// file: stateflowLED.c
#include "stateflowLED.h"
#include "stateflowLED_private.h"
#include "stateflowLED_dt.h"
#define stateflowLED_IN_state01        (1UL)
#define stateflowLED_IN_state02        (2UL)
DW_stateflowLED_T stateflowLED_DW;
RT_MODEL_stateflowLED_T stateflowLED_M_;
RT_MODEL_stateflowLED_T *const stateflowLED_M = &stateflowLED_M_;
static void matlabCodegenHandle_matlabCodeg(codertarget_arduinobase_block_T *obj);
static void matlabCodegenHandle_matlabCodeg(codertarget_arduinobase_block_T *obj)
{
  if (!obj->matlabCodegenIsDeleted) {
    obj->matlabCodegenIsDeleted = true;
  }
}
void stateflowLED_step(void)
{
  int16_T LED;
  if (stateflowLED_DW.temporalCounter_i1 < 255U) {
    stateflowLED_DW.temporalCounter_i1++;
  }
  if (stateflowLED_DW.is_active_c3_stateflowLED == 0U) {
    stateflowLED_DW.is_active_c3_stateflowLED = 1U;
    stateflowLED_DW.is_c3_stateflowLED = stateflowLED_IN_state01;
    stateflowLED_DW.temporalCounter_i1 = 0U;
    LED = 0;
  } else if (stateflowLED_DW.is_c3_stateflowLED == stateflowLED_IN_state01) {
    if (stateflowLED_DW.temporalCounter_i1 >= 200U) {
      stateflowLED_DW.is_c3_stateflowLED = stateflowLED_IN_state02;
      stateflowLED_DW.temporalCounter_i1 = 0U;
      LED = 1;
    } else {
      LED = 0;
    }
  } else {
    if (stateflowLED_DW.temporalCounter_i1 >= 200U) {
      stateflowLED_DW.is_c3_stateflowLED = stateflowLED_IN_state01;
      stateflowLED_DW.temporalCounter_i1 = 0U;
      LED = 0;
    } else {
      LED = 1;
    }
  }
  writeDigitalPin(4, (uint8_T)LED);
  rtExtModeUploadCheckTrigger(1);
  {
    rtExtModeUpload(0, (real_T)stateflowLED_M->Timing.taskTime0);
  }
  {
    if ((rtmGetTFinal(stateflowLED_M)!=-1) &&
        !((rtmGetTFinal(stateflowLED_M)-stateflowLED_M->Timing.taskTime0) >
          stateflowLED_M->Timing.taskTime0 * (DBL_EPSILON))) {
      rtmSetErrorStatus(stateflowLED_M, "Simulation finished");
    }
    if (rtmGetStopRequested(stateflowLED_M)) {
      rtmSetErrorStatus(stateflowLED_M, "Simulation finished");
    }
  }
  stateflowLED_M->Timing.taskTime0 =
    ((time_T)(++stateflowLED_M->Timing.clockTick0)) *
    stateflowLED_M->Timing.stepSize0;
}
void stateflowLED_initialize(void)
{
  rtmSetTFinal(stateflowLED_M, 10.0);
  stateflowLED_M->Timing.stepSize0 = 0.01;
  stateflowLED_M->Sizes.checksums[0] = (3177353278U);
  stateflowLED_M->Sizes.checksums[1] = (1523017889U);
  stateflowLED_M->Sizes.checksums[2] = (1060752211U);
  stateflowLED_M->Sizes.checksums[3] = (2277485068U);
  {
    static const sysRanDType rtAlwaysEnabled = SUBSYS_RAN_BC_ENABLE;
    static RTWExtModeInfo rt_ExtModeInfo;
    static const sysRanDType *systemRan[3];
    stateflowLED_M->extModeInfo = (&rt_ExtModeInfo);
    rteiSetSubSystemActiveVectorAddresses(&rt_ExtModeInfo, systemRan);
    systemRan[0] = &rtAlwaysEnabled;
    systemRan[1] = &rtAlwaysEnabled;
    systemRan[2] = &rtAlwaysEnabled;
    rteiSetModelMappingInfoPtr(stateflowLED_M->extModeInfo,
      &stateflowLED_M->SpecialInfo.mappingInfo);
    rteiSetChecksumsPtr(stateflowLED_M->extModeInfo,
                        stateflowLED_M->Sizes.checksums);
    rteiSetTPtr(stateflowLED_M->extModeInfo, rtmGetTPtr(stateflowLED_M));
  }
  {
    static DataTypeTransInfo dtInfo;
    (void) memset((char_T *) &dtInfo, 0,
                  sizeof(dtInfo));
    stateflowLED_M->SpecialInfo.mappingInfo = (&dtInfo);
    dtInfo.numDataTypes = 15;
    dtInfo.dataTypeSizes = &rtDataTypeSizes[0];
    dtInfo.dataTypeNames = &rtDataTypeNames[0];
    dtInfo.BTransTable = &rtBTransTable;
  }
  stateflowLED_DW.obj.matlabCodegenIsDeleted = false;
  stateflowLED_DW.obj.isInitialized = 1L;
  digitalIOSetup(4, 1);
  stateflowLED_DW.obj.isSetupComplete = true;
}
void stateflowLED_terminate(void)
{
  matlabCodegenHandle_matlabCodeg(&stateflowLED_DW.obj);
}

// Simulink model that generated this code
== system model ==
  DigitalOutput#1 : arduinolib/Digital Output  pinNumber=4  <- 1: Stateflowchart#1
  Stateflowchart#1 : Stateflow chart
== stateflow chart Stateflowchart#1 ==
  state state01
    LED=0;
  state state02
    LED=1;
  (default) -> state01
  state01 -> state02 : [after(2,sec)]
  state02 -> state01 : [after(2,sec)]
  data: LED output
